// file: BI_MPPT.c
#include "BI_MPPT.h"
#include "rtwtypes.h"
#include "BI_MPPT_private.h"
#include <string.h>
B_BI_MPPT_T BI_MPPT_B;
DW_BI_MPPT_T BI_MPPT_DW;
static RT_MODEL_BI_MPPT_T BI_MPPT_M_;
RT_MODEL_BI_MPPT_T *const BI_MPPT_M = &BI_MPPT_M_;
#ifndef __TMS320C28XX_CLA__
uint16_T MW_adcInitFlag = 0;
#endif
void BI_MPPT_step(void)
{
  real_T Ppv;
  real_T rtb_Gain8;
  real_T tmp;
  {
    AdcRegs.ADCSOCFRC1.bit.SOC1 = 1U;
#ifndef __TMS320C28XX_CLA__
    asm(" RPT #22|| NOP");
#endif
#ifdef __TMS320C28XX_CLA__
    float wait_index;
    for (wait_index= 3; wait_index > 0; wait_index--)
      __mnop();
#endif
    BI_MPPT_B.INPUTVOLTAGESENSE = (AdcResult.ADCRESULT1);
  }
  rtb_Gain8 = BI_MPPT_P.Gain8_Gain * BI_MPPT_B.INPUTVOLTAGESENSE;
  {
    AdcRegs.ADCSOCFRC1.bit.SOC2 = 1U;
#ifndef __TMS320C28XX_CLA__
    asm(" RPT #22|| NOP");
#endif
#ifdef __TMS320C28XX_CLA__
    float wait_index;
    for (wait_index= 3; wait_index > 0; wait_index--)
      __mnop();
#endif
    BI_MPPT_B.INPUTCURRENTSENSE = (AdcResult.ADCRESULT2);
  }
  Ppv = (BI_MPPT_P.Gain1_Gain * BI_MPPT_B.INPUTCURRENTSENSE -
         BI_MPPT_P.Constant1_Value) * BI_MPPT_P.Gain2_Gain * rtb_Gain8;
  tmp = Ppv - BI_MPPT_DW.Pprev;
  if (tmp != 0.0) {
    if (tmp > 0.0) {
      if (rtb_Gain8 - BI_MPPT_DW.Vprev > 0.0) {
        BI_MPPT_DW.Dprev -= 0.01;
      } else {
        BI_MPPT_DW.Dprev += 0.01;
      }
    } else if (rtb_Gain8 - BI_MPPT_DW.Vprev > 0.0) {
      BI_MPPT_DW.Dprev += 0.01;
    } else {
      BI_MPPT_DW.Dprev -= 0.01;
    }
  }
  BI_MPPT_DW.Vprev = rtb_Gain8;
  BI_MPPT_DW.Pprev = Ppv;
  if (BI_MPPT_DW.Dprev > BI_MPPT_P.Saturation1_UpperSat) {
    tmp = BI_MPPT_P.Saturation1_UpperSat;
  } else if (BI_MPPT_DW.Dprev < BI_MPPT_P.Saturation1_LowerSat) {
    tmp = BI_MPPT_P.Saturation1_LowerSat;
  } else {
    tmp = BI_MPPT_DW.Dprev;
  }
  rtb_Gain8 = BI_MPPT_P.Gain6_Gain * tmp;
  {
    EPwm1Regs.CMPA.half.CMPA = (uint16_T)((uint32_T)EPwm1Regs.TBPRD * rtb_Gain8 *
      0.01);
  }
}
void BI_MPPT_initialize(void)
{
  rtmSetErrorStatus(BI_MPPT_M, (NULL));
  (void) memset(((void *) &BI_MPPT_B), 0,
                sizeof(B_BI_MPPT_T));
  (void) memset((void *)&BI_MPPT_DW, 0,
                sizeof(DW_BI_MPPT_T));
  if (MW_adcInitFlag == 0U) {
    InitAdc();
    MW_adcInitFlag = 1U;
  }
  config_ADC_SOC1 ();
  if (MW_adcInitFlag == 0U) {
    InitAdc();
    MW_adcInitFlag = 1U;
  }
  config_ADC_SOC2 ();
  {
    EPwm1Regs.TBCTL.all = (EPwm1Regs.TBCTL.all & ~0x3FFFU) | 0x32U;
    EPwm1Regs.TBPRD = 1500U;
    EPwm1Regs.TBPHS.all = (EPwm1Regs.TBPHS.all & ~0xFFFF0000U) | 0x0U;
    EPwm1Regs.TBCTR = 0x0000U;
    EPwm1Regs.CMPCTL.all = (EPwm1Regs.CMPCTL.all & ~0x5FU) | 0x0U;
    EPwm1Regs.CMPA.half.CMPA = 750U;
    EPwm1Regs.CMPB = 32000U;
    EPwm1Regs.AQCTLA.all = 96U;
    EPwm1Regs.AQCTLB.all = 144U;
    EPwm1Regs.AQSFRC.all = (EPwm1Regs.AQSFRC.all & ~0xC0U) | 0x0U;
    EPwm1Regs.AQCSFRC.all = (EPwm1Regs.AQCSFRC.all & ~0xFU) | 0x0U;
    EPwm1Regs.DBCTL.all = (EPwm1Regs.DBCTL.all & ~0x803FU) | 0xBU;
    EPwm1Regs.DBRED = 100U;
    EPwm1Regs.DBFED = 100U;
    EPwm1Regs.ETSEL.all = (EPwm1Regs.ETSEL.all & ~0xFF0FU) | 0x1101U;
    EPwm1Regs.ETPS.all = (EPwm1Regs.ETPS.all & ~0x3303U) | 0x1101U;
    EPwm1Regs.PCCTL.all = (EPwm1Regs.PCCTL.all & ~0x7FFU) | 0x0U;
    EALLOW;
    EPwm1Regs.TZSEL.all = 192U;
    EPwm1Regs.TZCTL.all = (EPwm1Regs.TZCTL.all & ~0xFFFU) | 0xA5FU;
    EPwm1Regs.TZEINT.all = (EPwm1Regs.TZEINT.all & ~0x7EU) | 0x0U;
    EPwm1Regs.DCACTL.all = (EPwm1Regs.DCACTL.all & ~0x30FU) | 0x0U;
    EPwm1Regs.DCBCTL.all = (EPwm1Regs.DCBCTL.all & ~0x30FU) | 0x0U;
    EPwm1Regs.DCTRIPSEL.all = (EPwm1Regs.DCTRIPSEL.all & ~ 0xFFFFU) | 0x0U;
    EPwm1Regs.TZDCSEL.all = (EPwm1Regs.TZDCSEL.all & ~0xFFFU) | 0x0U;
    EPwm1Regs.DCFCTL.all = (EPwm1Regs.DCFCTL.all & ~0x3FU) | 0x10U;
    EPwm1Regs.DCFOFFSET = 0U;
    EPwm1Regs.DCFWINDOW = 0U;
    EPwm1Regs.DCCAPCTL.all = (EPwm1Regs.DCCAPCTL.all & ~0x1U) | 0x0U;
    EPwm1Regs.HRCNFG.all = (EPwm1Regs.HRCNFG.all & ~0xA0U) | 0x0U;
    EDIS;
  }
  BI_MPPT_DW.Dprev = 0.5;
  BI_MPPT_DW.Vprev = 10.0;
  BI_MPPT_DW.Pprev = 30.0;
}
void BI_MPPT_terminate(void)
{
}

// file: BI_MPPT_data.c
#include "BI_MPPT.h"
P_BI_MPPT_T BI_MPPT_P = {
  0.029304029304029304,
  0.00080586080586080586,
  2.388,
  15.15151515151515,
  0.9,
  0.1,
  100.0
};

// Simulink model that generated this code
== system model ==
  ePWM#1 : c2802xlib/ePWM  <- 1: Gain6
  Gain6 : Gain  Gain=100  <- 1: Saturation1
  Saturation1 : Saturate  UpperLimit=0.9  LowerLimit=0.1  <- 1: MATLABFunction#1
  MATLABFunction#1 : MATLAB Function  <- 1: Gain8, 2: Gain2
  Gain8 : Gain  Gain=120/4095  <- 1: INPUTVOLTAGESENSE
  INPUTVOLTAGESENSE : c2802xlib/ADC
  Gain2 : Gain  Gain=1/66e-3  <- 1: Sum#1
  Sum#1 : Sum  Inputs=+-  <- 1: Gain1, 2: Constant1
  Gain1 : Gain  Gain=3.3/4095  <- 1: INPUTCURRENTSENSE
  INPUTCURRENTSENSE : c2802xlib/ADC
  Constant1 : Constant  Value=2.388

